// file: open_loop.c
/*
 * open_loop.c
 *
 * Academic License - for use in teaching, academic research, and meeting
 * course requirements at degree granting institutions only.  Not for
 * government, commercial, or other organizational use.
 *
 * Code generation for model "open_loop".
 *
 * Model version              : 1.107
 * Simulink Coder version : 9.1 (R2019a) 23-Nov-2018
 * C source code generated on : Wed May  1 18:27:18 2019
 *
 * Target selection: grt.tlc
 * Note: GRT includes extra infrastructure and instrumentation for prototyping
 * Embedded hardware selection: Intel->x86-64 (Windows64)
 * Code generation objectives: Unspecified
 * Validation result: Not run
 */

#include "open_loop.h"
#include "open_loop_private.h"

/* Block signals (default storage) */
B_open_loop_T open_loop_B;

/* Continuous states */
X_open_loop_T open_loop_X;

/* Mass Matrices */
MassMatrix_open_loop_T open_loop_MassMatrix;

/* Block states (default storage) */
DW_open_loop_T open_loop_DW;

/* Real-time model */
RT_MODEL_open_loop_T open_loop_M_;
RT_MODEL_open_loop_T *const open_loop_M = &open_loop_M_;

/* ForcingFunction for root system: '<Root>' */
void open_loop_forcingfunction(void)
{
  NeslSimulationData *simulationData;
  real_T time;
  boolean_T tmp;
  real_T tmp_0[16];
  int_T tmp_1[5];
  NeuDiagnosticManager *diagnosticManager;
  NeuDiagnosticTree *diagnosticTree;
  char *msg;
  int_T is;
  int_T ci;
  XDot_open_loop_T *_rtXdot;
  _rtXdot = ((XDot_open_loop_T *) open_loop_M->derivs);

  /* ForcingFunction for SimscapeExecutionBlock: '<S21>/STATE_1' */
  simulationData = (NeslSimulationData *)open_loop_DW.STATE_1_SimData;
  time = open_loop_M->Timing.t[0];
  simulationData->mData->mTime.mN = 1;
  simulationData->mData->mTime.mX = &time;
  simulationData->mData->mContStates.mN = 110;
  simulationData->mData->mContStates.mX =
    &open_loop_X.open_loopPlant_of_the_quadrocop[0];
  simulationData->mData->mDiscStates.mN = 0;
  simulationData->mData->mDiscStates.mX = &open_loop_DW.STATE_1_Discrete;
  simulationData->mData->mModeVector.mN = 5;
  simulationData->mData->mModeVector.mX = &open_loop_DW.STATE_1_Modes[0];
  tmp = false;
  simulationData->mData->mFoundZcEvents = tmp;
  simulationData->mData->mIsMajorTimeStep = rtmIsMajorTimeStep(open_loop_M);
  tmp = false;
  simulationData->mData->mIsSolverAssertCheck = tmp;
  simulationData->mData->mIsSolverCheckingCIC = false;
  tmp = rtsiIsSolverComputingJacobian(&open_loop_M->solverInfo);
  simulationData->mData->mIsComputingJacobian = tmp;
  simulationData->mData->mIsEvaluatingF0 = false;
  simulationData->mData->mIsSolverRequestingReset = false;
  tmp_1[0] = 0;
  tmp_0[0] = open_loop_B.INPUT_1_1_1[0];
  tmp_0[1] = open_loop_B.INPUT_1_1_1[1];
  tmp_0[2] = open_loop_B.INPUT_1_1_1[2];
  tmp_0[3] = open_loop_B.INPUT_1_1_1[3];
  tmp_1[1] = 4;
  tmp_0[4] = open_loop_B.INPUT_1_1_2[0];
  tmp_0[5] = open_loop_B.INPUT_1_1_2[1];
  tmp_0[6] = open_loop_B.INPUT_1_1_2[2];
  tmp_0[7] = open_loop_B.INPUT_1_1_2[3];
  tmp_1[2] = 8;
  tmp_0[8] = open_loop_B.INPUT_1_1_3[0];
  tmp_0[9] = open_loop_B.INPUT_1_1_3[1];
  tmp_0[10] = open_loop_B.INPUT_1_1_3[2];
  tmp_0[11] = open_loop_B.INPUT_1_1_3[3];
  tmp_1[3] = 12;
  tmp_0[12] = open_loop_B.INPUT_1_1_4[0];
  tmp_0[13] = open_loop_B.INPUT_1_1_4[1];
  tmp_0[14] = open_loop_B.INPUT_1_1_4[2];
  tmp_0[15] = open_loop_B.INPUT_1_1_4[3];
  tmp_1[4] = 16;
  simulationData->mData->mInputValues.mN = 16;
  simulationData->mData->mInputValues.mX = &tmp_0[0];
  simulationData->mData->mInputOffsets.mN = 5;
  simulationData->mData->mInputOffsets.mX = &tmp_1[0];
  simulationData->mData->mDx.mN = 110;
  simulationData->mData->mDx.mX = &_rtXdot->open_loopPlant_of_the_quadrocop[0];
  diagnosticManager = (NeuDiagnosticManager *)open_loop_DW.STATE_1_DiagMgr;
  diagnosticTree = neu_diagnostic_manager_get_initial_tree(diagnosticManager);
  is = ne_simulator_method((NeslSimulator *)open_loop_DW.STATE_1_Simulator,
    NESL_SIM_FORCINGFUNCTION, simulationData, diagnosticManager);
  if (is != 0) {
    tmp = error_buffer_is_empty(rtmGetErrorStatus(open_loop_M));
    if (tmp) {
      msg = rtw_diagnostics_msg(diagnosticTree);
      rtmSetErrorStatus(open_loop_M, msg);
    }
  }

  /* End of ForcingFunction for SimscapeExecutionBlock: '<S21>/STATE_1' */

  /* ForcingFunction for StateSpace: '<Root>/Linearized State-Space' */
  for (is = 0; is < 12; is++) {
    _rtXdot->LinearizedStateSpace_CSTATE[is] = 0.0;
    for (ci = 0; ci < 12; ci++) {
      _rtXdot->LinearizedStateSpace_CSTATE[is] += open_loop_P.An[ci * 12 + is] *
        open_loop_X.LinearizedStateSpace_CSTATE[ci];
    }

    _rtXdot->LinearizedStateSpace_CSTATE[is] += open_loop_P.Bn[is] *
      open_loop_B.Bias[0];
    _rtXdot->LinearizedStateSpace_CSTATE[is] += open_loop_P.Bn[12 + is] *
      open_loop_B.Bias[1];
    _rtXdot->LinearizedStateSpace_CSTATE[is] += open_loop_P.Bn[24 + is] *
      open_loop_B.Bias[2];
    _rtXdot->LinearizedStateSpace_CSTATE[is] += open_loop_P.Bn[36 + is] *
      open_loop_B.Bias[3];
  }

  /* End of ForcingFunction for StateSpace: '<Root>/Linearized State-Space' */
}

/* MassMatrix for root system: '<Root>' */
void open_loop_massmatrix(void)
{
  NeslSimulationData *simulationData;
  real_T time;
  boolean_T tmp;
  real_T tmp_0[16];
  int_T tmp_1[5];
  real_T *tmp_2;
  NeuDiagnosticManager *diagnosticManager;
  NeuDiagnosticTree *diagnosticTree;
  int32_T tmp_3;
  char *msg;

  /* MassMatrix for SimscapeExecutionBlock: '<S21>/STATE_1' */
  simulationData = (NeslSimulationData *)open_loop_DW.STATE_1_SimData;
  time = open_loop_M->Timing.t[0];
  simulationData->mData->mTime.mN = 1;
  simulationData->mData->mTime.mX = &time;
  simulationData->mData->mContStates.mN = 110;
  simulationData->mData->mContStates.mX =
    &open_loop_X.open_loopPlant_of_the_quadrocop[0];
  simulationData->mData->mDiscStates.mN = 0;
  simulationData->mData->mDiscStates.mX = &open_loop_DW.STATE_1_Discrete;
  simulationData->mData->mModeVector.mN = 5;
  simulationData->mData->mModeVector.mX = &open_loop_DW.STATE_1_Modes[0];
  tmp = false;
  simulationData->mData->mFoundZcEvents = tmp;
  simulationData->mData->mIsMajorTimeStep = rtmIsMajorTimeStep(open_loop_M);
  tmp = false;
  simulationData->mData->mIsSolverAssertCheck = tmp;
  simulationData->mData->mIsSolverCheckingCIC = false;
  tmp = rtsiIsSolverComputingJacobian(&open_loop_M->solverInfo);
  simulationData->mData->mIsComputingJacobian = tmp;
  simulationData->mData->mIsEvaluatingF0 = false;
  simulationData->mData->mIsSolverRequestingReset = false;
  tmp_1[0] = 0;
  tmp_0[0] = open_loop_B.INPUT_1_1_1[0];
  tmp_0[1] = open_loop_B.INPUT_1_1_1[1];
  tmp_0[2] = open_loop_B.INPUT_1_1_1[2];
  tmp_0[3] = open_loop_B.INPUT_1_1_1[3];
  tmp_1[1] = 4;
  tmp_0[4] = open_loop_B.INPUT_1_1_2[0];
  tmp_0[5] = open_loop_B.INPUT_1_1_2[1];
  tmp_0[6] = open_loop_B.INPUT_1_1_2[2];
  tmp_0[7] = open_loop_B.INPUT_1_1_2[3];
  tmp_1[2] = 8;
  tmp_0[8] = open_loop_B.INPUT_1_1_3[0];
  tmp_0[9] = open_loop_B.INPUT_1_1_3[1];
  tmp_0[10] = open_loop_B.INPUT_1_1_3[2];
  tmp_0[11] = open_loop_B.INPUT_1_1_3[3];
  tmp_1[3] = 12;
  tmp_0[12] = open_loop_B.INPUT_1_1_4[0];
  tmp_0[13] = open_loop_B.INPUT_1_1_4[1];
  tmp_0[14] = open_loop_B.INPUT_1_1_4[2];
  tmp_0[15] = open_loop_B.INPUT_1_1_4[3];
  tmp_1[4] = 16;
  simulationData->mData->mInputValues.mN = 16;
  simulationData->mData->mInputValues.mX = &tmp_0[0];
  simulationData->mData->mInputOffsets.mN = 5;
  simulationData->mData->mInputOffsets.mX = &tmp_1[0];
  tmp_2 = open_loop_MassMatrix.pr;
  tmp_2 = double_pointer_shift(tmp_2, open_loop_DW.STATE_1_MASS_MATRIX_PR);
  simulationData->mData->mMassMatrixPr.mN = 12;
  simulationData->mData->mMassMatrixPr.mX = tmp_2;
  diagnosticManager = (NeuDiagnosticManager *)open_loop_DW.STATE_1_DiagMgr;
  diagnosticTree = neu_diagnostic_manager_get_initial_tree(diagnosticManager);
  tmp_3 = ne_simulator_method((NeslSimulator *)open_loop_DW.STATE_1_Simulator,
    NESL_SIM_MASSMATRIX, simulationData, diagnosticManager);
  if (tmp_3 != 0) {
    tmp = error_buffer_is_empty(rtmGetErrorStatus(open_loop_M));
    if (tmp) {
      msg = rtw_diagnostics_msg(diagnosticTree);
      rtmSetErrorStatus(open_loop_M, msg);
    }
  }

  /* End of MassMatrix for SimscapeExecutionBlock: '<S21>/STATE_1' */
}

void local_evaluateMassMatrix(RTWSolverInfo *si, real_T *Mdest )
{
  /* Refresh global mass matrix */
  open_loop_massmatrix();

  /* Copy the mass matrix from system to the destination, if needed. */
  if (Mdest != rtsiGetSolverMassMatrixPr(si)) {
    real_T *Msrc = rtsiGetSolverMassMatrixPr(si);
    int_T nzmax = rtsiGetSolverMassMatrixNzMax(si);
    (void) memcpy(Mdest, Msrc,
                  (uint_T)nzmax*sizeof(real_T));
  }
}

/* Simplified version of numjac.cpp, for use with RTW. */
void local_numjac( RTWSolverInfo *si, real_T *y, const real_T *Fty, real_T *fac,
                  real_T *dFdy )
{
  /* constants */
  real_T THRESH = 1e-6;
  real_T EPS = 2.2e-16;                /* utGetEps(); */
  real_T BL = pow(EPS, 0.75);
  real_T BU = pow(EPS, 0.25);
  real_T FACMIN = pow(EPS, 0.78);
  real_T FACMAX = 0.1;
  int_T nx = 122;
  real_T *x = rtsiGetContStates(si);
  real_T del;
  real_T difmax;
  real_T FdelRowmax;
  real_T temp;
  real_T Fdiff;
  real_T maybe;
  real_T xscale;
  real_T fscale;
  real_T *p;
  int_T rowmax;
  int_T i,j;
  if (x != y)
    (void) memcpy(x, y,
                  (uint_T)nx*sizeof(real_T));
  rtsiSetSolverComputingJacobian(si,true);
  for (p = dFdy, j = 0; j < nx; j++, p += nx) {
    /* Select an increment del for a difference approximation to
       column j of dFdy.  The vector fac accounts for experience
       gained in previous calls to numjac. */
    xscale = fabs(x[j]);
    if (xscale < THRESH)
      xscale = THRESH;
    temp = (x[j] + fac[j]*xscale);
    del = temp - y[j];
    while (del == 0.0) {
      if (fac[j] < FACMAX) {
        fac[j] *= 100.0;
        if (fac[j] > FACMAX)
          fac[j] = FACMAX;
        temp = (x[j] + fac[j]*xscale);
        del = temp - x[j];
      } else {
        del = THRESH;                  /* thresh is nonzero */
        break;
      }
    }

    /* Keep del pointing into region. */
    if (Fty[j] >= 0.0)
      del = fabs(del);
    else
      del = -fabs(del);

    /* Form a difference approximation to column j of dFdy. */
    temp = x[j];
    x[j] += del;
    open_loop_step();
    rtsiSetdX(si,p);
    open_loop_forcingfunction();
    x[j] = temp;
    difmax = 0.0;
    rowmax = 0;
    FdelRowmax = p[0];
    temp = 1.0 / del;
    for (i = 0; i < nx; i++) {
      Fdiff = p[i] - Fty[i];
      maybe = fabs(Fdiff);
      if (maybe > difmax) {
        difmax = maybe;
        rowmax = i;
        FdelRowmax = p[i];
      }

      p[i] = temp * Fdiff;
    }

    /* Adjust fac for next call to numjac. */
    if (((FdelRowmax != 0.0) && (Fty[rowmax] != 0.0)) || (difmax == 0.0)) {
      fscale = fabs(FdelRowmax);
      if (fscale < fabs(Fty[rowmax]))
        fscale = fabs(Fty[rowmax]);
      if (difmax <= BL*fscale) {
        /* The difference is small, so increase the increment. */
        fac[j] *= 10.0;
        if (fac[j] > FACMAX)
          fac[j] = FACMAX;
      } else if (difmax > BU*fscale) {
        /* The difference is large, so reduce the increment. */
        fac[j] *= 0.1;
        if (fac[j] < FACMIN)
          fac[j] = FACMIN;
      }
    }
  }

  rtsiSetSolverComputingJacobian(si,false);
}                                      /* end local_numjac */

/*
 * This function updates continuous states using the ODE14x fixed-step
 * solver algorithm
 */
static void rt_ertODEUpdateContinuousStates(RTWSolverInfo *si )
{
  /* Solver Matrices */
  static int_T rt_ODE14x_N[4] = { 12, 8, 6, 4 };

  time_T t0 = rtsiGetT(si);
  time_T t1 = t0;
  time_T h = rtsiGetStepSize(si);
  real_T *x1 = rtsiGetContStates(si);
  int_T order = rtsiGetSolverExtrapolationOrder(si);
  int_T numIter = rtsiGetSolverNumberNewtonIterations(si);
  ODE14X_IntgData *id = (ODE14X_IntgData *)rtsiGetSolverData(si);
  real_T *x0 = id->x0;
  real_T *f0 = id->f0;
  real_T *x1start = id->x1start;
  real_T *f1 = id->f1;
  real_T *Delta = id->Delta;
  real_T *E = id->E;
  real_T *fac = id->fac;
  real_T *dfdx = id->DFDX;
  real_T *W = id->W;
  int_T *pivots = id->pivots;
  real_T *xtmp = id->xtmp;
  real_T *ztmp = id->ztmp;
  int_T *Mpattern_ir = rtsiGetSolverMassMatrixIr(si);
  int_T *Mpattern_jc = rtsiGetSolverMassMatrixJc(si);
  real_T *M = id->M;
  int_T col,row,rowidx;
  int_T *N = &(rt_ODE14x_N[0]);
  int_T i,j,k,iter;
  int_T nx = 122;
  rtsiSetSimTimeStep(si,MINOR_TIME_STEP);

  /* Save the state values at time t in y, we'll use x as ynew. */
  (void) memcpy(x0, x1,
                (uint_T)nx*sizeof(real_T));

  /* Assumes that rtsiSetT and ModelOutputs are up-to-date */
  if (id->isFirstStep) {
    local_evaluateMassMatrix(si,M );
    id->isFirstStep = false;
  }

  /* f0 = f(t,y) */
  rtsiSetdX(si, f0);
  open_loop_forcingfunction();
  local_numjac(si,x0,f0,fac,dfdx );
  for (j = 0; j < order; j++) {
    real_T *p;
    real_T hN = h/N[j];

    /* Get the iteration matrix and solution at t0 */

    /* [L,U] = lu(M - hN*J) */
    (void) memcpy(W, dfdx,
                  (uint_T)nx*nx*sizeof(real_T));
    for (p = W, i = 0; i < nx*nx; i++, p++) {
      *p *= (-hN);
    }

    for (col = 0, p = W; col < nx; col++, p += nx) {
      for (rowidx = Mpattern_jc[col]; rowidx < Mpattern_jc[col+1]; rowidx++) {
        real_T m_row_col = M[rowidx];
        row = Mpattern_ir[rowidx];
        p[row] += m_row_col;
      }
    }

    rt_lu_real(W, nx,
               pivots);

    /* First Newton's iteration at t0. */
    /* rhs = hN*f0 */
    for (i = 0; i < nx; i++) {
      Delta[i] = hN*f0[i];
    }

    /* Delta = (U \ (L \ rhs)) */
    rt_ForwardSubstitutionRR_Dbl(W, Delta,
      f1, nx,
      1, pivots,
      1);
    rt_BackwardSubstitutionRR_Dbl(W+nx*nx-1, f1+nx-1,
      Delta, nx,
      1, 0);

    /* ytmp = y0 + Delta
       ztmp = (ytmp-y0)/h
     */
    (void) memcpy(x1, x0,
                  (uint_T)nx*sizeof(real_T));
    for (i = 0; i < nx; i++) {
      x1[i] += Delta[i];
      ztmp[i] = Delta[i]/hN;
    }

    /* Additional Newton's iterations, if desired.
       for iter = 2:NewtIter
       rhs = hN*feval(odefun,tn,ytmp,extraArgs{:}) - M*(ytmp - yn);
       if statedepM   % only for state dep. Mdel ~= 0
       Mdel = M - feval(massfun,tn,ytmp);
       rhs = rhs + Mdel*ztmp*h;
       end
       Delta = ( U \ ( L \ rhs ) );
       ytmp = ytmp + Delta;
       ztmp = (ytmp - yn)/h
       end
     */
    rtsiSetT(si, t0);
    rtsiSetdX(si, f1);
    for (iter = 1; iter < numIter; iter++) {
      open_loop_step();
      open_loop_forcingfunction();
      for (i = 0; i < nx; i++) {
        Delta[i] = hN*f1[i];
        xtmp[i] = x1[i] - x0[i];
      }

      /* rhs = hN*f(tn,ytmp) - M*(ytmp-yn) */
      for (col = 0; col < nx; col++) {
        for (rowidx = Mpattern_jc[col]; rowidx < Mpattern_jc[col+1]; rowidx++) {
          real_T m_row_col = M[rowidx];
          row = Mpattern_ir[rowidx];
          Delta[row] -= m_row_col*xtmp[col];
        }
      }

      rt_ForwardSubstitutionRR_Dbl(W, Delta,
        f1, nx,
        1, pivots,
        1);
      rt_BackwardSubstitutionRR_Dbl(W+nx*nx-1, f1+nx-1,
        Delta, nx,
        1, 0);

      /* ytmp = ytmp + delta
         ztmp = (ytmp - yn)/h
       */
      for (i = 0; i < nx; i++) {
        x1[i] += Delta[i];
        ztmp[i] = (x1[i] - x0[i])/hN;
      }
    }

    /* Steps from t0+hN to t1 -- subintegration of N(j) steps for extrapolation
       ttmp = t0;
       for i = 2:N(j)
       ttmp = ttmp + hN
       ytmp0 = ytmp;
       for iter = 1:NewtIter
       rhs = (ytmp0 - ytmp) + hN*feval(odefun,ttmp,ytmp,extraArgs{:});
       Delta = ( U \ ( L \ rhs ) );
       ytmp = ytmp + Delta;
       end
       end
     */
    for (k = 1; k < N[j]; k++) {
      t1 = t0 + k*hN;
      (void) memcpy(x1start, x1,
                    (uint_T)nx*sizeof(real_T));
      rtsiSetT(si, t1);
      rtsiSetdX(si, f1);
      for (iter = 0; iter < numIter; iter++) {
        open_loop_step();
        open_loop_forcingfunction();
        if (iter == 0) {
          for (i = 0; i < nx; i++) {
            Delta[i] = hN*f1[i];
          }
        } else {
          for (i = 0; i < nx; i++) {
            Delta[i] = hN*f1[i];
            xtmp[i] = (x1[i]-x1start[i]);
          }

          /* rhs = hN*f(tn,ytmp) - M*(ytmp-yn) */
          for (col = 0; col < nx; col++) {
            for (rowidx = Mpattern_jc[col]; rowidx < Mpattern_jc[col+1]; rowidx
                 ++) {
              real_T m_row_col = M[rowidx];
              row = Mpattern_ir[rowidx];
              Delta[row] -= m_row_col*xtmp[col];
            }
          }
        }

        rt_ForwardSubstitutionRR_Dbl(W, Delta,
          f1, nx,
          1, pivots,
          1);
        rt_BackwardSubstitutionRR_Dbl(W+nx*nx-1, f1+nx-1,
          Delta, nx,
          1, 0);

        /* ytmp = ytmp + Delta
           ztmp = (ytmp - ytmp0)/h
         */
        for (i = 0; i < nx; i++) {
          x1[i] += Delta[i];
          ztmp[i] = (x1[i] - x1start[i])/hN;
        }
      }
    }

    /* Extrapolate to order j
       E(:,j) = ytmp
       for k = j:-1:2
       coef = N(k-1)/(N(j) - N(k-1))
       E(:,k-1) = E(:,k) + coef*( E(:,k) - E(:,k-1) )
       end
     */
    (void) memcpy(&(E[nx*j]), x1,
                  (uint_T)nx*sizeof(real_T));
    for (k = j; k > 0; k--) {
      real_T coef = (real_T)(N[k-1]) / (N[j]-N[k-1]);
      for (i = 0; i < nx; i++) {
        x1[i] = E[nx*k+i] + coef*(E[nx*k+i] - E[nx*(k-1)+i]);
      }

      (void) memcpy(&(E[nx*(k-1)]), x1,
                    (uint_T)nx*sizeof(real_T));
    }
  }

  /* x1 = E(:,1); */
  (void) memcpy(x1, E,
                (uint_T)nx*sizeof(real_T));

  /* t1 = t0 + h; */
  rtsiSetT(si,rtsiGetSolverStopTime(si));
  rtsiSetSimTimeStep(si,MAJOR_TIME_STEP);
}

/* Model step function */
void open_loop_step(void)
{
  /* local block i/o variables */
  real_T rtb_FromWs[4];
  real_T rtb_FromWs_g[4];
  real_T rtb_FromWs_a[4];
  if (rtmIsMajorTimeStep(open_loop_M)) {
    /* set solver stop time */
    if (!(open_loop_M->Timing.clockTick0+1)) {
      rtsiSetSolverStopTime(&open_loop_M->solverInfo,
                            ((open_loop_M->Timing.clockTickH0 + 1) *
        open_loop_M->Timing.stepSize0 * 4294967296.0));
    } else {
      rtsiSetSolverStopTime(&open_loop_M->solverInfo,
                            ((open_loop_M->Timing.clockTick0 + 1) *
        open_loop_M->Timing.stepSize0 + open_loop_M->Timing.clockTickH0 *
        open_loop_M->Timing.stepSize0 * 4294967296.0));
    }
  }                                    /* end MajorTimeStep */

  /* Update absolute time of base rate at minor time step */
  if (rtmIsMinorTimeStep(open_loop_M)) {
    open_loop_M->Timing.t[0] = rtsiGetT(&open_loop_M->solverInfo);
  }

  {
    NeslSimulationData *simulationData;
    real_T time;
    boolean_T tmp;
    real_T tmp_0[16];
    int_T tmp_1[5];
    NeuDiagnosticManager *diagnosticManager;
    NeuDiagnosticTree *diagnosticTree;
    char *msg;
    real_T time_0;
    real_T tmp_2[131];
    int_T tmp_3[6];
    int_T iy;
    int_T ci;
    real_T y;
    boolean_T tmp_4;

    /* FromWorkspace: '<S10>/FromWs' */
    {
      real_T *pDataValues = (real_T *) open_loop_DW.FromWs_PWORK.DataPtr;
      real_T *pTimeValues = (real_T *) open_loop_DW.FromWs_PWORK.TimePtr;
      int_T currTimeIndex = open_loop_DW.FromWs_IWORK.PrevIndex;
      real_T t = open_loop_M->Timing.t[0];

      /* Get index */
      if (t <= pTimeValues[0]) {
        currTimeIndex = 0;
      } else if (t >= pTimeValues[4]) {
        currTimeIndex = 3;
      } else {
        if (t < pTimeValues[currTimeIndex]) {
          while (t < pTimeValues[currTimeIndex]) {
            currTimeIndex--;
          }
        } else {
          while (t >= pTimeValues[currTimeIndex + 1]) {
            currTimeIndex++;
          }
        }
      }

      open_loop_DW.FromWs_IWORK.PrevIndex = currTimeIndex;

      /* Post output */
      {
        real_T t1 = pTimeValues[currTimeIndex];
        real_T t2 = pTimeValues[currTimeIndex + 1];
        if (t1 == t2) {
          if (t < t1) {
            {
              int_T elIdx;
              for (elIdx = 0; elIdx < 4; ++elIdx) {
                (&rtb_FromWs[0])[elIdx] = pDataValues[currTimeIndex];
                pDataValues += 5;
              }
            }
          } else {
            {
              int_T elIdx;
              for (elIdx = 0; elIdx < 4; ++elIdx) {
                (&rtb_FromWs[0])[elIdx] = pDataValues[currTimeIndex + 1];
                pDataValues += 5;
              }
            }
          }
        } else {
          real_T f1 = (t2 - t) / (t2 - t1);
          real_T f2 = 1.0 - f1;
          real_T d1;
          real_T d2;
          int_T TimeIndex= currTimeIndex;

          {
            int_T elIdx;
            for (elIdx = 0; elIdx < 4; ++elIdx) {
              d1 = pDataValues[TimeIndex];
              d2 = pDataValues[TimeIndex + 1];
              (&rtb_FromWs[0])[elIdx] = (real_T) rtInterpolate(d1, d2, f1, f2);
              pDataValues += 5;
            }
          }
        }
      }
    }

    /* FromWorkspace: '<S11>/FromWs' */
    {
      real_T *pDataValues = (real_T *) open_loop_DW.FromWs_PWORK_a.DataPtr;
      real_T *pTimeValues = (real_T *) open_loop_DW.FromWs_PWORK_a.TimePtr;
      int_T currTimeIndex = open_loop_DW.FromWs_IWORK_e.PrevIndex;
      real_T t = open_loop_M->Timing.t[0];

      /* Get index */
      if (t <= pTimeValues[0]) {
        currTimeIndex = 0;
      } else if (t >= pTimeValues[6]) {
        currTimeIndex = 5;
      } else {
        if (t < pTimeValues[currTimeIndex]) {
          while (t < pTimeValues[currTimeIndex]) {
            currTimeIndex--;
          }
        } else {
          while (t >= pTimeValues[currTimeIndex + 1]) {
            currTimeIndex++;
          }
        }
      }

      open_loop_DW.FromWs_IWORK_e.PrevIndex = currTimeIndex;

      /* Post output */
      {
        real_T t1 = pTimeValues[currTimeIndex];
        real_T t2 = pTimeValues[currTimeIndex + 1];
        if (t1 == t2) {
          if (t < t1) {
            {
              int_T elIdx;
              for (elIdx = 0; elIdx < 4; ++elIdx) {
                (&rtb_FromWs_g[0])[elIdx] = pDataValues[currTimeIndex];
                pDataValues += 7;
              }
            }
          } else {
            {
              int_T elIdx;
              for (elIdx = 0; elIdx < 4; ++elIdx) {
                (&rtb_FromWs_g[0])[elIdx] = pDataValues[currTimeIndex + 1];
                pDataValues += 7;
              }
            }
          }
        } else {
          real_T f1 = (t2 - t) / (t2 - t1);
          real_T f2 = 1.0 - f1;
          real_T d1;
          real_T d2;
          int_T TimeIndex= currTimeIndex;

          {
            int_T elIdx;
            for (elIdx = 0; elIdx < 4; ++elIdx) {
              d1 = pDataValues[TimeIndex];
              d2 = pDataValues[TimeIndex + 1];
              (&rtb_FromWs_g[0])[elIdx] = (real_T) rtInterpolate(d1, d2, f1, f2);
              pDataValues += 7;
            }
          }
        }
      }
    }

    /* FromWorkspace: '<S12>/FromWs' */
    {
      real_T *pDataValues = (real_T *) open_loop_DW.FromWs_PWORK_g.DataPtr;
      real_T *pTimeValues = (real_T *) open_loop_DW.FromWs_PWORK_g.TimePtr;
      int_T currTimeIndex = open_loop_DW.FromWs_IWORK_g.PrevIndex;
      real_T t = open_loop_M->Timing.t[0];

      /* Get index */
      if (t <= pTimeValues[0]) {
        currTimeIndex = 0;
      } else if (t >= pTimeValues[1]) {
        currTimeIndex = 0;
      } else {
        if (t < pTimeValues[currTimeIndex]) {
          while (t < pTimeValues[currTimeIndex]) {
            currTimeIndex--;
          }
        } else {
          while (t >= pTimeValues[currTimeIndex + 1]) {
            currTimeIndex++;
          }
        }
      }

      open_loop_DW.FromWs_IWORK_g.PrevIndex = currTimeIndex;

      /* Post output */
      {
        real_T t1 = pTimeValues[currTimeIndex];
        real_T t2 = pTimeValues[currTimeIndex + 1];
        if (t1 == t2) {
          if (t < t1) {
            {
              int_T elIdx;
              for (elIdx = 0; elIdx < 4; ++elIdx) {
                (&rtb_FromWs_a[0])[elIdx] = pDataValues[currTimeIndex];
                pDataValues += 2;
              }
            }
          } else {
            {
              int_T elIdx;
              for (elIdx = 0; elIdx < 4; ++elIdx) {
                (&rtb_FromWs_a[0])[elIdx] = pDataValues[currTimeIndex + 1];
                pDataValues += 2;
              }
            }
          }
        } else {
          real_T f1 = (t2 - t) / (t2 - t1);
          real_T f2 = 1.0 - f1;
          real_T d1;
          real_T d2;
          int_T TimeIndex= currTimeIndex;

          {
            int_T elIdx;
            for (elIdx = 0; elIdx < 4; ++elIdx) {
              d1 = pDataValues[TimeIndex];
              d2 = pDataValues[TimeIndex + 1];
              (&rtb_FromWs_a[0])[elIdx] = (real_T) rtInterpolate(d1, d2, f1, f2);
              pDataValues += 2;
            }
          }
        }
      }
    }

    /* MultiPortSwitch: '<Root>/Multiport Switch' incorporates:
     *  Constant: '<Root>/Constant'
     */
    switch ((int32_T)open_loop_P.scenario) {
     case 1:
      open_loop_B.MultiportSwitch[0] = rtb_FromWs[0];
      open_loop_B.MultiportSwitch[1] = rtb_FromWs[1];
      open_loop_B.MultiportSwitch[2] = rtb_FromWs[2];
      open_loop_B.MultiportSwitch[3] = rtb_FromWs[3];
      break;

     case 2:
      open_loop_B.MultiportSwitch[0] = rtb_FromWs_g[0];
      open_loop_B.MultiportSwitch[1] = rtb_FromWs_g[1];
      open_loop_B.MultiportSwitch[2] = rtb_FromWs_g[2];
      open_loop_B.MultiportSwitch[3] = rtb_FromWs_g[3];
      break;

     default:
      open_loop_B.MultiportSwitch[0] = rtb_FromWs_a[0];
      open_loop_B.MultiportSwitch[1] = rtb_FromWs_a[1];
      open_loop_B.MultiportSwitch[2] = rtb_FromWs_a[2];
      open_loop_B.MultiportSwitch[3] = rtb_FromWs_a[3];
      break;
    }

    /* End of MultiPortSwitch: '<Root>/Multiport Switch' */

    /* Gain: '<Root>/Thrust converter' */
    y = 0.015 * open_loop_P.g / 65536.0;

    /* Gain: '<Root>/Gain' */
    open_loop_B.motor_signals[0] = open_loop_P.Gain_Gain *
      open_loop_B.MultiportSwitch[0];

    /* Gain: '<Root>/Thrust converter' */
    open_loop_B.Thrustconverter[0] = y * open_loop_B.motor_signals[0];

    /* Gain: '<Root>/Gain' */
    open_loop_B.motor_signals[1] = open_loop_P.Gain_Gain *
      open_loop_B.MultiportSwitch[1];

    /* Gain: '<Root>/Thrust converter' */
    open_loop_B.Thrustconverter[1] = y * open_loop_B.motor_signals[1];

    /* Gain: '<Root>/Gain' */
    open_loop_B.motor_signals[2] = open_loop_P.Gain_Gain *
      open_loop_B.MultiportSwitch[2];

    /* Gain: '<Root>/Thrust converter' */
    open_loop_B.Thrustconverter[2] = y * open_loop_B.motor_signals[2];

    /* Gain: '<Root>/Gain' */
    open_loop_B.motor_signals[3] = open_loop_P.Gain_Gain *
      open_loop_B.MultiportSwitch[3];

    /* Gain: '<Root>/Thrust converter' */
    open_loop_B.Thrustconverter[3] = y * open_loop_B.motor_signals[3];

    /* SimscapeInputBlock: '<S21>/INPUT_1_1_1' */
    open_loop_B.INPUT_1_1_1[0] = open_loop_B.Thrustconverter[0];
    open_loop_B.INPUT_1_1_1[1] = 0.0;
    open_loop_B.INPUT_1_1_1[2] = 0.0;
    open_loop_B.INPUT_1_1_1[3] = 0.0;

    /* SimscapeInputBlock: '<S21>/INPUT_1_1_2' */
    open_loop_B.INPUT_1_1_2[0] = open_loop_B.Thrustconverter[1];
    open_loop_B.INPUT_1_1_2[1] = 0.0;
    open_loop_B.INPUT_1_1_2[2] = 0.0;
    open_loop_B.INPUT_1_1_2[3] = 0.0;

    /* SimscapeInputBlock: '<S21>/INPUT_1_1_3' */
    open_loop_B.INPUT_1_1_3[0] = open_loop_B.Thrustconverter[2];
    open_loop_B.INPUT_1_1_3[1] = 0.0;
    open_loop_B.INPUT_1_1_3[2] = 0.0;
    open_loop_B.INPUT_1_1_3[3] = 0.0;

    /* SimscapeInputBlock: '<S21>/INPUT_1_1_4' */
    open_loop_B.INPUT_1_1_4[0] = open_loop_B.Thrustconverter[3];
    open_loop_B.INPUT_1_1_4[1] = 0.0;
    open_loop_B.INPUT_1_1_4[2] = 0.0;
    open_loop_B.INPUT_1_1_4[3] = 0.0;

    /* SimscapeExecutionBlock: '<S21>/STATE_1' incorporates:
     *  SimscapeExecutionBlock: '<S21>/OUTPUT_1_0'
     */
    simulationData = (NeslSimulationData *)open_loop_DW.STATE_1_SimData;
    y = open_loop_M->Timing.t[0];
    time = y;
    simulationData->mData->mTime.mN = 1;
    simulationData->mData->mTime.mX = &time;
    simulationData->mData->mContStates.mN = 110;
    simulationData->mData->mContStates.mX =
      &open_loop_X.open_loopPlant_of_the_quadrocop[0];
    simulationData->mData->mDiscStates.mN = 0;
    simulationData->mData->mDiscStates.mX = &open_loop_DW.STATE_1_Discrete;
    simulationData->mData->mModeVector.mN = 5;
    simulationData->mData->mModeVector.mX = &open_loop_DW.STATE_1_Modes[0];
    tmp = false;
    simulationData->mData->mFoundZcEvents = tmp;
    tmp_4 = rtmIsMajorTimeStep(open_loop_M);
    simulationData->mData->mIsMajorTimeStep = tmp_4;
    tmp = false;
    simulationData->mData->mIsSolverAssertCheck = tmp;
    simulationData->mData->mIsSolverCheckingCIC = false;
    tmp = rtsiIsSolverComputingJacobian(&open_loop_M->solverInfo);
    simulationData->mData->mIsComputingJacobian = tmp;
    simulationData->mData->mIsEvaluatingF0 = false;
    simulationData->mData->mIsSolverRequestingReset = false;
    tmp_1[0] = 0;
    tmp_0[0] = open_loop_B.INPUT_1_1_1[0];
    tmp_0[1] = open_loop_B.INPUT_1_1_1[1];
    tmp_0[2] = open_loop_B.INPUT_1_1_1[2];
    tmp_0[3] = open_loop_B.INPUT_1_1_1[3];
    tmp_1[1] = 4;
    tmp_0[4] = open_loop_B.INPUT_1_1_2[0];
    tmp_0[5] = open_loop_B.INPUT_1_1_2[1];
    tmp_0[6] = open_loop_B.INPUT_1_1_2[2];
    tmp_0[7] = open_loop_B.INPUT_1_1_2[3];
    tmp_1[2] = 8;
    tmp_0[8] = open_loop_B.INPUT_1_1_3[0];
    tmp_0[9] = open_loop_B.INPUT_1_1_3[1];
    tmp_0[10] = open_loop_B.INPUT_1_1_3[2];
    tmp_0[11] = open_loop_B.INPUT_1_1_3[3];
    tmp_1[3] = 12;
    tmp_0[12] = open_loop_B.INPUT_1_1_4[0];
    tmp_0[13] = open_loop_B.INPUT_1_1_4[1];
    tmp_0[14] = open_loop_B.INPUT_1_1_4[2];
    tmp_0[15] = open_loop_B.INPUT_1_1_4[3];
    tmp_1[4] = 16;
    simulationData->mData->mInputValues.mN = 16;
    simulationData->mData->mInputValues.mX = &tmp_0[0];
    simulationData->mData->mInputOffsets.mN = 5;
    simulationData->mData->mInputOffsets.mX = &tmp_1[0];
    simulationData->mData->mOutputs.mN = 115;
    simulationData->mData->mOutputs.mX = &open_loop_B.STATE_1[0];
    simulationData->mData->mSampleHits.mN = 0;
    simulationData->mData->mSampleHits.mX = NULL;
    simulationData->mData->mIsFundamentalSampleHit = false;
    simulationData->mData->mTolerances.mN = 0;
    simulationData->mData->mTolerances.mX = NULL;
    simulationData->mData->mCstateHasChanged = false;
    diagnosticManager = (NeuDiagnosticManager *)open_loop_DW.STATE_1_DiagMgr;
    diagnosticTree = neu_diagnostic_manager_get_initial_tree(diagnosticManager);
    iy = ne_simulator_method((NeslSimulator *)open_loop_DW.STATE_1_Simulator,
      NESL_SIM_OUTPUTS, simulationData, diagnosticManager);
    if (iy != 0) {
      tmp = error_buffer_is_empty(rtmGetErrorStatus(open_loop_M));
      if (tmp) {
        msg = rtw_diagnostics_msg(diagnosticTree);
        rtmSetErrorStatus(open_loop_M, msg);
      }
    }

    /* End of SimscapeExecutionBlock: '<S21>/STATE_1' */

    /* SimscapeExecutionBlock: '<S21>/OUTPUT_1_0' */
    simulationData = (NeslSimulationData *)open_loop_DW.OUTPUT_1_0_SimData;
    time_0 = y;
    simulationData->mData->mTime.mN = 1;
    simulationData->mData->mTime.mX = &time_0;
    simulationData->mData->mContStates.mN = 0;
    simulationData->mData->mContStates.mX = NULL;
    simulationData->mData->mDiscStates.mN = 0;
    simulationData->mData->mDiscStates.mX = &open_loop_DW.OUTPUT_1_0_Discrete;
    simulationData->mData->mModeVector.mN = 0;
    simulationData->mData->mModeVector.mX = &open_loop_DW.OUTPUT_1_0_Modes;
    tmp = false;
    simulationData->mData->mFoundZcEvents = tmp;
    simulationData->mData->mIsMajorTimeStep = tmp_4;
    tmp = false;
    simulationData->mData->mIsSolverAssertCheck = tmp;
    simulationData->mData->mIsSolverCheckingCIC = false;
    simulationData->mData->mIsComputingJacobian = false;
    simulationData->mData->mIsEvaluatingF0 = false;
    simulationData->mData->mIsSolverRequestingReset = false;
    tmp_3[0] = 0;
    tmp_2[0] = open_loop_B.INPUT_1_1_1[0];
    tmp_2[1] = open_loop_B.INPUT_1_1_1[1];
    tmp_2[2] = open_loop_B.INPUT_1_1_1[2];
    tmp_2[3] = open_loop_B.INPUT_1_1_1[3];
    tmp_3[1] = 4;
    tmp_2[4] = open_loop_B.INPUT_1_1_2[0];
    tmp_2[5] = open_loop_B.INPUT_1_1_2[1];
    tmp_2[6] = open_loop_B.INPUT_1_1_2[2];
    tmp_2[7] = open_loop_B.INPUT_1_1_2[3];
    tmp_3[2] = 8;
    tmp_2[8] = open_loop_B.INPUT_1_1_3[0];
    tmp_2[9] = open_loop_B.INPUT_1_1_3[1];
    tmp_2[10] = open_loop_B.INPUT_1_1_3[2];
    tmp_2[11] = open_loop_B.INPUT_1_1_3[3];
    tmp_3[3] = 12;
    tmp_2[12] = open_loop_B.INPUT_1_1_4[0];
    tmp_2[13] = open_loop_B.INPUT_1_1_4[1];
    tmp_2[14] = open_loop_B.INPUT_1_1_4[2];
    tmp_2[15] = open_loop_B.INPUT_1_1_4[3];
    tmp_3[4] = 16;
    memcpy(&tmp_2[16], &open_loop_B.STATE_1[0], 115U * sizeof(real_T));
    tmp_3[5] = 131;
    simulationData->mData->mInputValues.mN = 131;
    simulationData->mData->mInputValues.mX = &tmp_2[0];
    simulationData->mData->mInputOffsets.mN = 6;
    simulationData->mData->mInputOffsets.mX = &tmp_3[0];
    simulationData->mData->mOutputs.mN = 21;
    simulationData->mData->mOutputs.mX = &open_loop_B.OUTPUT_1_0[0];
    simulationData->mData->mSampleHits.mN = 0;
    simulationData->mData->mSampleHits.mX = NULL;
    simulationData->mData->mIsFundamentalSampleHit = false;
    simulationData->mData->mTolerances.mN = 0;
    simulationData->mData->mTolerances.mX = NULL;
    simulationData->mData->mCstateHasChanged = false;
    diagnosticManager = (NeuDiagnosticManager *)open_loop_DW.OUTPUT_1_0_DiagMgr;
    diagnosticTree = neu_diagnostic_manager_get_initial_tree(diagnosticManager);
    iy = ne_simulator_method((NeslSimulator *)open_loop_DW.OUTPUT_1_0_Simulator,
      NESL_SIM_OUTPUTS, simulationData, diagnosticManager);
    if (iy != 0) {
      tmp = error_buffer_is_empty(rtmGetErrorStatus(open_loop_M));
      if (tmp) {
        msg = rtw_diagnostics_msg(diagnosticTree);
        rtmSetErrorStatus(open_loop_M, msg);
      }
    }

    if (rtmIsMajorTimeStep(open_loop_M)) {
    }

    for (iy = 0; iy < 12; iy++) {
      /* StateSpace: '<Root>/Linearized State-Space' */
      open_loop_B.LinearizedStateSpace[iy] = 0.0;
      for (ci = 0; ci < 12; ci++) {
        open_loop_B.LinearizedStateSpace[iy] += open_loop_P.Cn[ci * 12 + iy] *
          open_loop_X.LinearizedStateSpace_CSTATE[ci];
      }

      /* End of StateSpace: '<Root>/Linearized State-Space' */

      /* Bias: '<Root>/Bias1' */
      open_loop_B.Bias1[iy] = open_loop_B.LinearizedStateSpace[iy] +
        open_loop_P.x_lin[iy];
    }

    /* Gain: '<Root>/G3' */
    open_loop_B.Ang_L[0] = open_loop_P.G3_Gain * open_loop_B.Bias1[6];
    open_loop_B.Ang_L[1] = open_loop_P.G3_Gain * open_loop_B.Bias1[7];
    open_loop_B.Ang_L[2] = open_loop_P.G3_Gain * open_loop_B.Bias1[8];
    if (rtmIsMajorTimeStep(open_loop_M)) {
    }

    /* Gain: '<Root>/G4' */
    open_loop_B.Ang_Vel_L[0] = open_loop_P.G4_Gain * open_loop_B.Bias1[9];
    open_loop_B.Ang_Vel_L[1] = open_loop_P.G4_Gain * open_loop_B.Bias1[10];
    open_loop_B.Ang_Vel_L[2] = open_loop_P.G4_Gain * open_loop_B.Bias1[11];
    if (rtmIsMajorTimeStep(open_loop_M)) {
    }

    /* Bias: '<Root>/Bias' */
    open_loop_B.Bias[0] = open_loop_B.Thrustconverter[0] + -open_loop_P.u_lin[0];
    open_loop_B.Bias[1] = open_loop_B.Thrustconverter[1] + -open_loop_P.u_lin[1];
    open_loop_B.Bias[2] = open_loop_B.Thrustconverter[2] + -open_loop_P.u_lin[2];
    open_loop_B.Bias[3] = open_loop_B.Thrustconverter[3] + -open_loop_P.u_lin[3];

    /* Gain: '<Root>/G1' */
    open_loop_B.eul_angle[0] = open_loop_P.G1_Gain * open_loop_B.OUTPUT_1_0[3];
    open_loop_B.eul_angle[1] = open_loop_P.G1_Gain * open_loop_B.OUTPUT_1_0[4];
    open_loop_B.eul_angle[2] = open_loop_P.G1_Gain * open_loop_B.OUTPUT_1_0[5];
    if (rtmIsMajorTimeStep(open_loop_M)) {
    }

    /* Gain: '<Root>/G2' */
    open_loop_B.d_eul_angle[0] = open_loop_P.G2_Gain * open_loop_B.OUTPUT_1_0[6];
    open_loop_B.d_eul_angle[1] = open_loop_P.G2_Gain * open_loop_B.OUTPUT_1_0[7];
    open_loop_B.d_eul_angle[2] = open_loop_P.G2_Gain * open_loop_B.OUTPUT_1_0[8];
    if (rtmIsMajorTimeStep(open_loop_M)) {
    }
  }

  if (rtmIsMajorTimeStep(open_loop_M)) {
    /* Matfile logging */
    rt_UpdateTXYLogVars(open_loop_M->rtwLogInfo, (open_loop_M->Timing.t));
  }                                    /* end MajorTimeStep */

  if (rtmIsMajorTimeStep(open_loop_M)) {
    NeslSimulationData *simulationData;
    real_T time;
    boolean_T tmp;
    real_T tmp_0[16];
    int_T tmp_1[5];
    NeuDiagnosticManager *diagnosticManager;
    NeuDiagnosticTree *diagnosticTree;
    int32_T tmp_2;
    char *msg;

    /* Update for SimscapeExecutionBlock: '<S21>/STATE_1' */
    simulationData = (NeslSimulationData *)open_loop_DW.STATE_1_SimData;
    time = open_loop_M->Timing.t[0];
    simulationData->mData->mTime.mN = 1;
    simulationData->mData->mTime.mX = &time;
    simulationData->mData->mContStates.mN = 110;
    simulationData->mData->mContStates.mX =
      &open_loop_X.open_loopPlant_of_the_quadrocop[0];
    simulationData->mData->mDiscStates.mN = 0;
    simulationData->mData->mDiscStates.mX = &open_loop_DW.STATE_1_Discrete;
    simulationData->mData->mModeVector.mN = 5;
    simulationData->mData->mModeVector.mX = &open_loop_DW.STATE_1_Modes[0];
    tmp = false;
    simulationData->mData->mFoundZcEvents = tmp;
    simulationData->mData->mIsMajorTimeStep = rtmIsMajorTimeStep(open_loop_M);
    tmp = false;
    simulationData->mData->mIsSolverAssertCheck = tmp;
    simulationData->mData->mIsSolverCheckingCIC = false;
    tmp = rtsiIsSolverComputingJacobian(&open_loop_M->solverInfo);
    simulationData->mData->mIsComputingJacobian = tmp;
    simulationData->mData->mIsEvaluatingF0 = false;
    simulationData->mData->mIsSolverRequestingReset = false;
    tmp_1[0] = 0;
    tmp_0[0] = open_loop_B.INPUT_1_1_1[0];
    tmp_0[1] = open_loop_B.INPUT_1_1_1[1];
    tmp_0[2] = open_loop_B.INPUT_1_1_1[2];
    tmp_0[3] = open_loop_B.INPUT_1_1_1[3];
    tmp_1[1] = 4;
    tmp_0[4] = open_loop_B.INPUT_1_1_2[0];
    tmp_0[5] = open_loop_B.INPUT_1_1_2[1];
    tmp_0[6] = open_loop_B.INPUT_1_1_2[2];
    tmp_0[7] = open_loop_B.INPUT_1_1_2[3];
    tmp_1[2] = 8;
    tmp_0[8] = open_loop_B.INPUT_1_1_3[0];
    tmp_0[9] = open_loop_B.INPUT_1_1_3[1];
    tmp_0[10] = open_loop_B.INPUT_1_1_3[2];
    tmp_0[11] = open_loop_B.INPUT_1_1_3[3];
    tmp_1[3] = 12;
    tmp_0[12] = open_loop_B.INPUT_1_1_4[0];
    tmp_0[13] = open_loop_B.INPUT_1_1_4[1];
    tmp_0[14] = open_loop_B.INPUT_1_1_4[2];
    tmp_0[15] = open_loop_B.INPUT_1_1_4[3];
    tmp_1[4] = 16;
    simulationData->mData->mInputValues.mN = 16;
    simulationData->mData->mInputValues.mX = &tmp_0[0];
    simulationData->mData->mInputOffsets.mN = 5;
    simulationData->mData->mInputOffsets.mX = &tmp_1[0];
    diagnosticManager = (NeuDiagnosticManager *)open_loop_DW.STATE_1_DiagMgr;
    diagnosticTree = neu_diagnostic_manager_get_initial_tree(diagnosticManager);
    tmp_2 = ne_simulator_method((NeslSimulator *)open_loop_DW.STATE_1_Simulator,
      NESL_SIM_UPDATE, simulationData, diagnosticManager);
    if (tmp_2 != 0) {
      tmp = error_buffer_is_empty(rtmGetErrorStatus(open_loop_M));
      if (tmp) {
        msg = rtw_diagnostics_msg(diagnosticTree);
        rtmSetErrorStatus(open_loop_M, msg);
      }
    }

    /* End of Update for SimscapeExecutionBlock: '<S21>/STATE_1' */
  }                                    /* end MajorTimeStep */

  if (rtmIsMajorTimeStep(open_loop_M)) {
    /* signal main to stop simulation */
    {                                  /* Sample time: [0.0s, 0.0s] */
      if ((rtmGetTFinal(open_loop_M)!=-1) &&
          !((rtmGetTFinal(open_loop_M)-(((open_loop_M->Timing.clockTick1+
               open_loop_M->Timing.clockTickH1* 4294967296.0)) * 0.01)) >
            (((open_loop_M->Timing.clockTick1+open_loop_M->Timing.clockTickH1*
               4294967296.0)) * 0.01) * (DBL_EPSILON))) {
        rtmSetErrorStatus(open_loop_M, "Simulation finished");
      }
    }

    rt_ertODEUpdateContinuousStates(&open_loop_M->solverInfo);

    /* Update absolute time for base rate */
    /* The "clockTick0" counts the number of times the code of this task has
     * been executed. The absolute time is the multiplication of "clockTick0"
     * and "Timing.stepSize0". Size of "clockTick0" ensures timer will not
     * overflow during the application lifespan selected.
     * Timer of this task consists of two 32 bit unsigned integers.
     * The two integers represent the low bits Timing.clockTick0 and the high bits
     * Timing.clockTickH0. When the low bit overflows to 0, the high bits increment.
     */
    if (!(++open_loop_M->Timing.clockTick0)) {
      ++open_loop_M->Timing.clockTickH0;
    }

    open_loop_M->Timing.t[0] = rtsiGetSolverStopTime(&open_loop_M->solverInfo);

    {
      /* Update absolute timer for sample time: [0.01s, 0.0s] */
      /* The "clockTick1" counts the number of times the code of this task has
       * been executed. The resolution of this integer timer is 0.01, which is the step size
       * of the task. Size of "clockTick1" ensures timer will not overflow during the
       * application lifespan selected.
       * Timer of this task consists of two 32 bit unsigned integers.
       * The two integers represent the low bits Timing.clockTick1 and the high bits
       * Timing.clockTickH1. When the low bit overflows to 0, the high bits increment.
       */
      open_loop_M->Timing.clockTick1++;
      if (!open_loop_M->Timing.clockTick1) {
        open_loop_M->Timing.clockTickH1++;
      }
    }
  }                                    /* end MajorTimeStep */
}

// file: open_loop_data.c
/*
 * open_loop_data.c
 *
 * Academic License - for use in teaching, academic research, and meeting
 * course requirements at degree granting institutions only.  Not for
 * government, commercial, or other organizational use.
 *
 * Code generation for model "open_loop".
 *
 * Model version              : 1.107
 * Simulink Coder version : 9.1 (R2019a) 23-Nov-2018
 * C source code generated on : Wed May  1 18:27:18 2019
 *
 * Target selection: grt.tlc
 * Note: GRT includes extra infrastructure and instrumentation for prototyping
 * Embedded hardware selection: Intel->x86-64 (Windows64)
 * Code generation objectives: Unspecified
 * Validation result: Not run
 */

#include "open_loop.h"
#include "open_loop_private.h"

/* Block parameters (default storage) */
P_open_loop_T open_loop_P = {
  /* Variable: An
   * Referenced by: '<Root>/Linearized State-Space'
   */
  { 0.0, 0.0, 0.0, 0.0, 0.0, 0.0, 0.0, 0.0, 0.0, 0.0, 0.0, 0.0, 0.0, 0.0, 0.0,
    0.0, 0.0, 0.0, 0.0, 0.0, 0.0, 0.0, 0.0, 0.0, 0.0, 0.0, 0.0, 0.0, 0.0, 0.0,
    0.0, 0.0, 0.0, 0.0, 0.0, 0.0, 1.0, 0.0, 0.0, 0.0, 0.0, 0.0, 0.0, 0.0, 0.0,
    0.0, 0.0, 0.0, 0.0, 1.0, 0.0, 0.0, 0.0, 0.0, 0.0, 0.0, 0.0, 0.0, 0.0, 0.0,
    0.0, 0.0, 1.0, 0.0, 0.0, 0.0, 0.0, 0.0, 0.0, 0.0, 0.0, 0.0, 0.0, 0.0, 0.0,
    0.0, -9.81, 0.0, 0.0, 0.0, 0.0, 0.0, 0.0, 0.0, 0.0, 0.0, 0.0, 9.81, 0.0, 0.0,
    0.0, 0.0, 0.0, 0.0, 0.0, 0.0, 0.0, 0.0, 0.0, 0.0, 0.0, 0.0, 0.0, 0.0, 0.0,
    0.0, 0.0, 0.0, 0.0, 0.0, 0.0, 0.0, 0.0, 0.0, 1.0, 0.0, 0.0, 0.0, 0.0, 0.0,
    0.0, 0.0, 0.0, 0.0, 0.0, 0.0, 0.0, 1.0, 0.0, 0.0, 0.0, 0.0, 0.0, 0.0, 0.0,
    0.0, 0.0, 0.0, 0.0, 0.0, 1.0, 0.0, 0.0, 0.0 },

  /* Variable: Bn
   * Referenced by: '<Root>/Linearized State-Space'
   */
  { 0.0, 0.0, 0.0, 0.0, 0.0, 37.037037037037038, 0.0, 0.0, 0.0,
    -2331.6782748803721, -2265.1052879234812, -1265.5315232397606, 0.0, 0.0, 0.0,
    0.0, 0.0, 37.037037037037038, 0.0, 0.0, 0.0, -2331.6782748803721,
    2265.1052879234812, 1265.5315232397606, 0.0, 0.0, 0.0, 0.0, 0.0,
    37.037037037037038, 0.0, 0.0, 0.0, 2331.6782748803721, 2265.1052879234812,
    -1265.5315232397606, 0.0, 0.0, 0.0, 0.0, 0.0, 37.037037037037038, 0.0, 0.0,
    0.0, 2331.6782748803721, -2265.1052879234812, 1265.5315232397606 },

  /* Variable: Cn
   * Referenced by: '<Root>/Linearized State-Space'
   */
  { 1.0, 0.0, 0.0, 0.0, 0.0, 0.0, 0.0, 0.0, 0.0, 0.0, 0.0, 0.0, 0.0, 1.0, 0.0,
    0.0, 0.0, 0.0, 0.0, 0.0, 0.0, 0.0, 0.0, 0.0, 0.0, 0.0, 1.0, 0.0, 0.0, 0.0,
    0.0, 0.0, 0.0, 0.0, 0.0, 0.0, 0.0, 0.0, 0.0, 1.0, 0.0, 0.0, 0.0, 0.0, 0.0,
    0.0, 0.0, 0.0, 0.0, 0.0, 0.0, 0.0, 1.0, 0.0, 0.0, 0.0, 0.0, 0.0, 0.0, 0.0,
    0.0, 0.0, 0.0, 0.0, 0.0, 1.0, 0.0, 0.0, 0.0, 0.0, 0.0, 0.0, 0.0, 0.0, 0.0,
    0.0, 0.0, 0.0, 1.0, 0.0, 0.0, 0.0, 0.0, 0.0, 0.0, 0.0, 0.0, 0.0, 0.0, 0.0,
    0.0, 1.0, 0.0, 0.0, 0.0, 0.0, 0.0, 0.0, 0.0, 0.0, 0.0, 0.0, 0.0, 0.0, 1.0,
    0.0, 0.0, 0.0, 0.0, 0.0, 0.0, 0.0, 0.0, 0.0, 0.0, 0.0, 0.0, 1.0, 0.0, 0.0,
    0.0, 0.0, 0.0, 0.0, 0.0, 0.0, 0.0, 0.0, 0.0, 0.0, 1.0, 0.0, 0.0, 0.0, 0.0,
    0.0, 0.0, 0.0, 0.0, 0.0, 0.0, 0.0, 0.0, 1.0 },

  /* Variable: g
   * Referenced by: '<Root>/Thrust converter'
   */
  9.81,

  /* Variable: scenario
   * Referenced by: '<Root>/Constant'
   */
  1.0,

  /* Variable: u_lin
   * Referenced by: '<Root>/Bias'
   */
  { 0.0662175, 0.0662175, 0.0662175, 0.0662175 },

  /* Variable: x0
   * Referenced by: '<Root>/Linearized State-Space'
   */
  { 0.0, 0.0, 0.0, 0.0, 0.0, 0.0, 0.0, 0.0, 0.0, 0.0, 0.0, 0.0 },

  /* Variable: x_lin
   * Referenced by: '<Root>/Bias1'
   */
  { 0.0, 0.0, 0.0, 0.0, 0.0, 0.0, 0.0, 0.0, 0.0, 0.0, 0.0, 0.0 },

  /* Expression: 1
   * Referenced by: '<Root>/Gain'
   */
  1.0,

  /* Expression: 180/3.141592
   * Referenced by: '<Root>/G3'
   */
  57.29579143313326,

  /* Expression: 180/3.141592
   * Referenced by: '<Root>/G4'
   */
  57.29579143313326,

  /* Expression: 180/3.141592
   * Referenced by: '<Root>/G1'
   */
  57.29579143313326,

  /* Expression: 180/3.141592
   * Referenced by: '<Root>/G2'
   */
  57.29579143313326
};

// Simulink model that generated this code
simulink model "open_loop"  (R2019a)
settings: Solver=FixedStepAuto  StartTime=0.0  StopTime=10.0  FixedStep=1/100  RelTol=1e-3  AbsTol=1e-3
model workspace: external: MATLAB File params.m (data not in the file)
values from neighbouring files (symbols this model uses):
  An = double(subs(A, [x;ctrl] , [x_lin; u_lin] ))    [linearization.m]
  b = 2.75E-11    (= 2.75e-11)    [linearization.m]    (also in main.m)
  Bn = double(subs(B, [x;ctrl] , [x_lin; u_lin] ))    [linearization.m]
  Cn = eye(size(x,1))    [linearization.m]
  Dn = zeros(size(x,1),4)    [linearization.m]
  g = 9.81    [linearization.m]    (also in main.m)
  k = 1E-9    (= 1e-09)    [linearization.m]    (also in main.m)
  m = 0.027    [linearization.m]    (also in main.m)
  scenario = 1    [main.m]
  u_lin = repmat(0.027*g/4, [4 1])    [main.m]
  x0 = [0 0 0  0 0 0  deg2rad(20) deg2rad(20) deg2rad(0) 0 0 0]'    [main.m]
  x_lin = zeros(12,1)    [main.m]
undefined symbols (not defined in the file or in its folder): sigbuilder_block
libraries: nesl_utility x9

== system open_loop ==
  note: Input generator
      | (type should be uint16)
  note: Plant model
  Acc. data : Scope
  Acceleration : Scope
  Ang_L : Scope
  Ang_vel_L : Scope
  Angle : Scope
  Angular velocity : Scope
  Bias : Bias  Bias=-u_lin
  Bias1 : Bias  Bias=+x_lin
  Constant : Constant  Value=scenario
  Demux : Demux
  G{1..4} (4 alike) : Gain  Gain=180/3.141592
  Gain : Gain
  Gyro. data : Scope
  Linearized State-Space : StateSpace  A=An  B=Bn  C=Cn  D=Dn  InitialCondition=x0
  MotorSignals : Scope
  Multiport Switch : MultiPortSwitch
  Mux1 : Mux
  Mux2 : Mux
  Mux3 : Mux
  PS -> S {1..7} (7 alike) : nesl_utility/PS-Simulink Converter  PhysicalDomain=network_engine_domain  SubClassName=ps_output  LeftPortType=input  RightPortType=output  PseudoPeriodic=off  Frequencies=[]  Unit=1  AffineConversion=off
  Plant of the quadrocopter : SimscapeComponentBlock  SourceFile=plant  ComponentPath=plant  ComponentVariants=plant  ComponentVariantNames=plant  ClassName=plant  SchemaVersion=1  m=m kg  g=g m/s^2  d=d m  k=k s^2*N/rad^2  b=b N*m/(rad/s)^2
  Plant of the quadrocopter1 : SimscapeComponentBlock  SourceFile=sensors  ComponentPath=sensors  ComponentVariants=sensors  ComponentVariantNames=sensors  ClassName=sensors  SchemaVersion=1  m=m kg  g=g m/s^2  d=d m  k=k  b=b
  Pos_L : Scope
  Position : Scope
  Simulink-PS Converter : nesl_utility/Simulink-PS Converter  PhysicalDomain=network_engine_domain  SubClassName=ps_input  LeftPortType=input  RightPortType=output  PseudoPeriodic=off  Frequencies=[]  NoiseDistribution=none  NoiseParameters=[]  Unit=1  AffineConversion=off  FilteringAndDerivatives=zero  SimscapeFilterOrder=1  InputFilterTimeConstant=0.001  UdotUserProvided=1
  Solver Configuration : nesl_utility/Solver Configuration  PhysicalDomain=network_engine_domain  SubClassName=solver  LeftPortType=input  RightPortType=generic  Tones=[]  Harmonics=[]  SimulateNoise=off  Profile=off  UseLocalSampling=off  EnableSwitchedLinearOptims=on  FrequencyDomain=off  UseCCode=off  RelTol=0.001  AbsTol=1e-06  MinStep=1e-09  ToWorkspace=off  RevertToSquareIcSolve=off  NumHomotopyIterations=100  PhasorMode=off  PhasorModeNumHarmonics=1  DoDC=off  ResidualTolerance=1e-09  UseLocalSolver=off  LocalSolverChoice=NE_BACKWARD_EULER_ADVANCER  LocalSolverSampleTime=0.001  DoFixedCost=off  MaxNonlinIter=3  MaxModeIter=2  LinearAlgebra=Sparse  EquationFormulation=NE_TIME_EF  DelaysMemoryBudget=1024  AutomaticFiltering=on  FilteringTimeConstant=0.001  PartitionStorageMethod=AS_NEEDED  PartitionMemoryBudget=1024  PartitionMethod=FAST
  Thrust : Scope
  Thrust converter : Gain  Gain=0.06/4*g/65536
  ToDouble : DataTypeConversion  OutDataTypeStr=double  RndMeth=Round  SaturateOnIntegerOverflow=on
  Vel_L : Scope
  Velocity : Scope
  scenario 1 : Subsystem  Tag=STV Subsys  LoadFcn=sigbuilder_block('load');  StartFcn=sigbuilder_block('start');  StopFcn=sigbuilder_block('stop');  ClipboardFcn=sigbuilder_block('clipboard');  mask(Sigbuilder block){tuvar=[0:10]}
      mask help: Simulink:masks:SigbuilderBlock_MD
      mask init:
      | if ~strcmp(get_param(bdroot(gcbh),'SimulationStatus'),'stopped') tuvar = sigbuilder_block('maskInit'); end
  scenario 2 : Subsystem  Tag=STV Subsys  LoadFcn=sigbuilder_block('load');  StartFcn=sigbuilder_block('start');  StopFcn=sigbuilder_block('stop');  ClipboardFcn=sigbuilder_block('clipboard');  mask(Sigbuilder block){tuvar=[0:10]}
      mask help: Simulink:masks:SigbuilderBlock_MD
      mask init:
      | if ~strcmp(get_param(bdroot(gcbh),'SimulationStatus'),'stopped') tuvar = sigbuilder_block('maskInit'); end
  scenario 3 : Subsystem  Tag=STV Subsys  LoadFcn=sigbuilder_block('load');  StartFcn=sigbuilder_block('start');  StopFcn=sigbuilder_block('stop');  ClipboardFcn=sigbuilder_block('clipboard');  mask(Sigbuilder block){tuvar=[0:10]}
      mask help: Simulink:masks:SigbuilderBlock_MD
      mask init:
      | if ~strcmp(get_param(bdroot(gcbh),'SimulationStatus'),'stopped') tuvar = sigbuilder_block('maskInit'); end
  wires:
  "PS -> S 7"/1 -> Gyro. data/1  "gyro_data"
  "PS -> S 6"/1 -> Acc. data/1  "acc_data"
  Multiport Switch/1 -> Gain/1
  G1/1 -> Angle/1  "eul_angle"
  G2/1 -> Angular velocity/1  "d_eul_angle"
  ToDouble/1 -> Thrust converter/1
  Thrust converter/1 -> Bias/1, Simulink-PS Converter/1, Thrust/1
  "PS -> S 1"/1 -> Position/1  "pos"
  "PS -> S 5"/1 -> G2/1
  "PS -> S 4"/1 -> G1/1
  "PS -> S 3"/1 -> Acceleration/1  "acc"
  "PS -> S 2"/1 -> Velocity/1  "vel"
  scenario 1/2(Signal 2) -> Mux3/2
  scenario 1/1(Signal 1) -> Mux3/1
  scenario 1/3(Signal 3) -> Mux3/3
  scenario 1/4(Signal 4) -> Mux3/4
  scenario 2/3(Signal 3) -> Mux1/3
  scenario 2/4(Signal 4) -> Mux1/4
  scenario 2/2(Signal 2) -> Mux1/2
  Mux1/1 -> Multiport Switch/3
  scenario 2/1(Signal 1) -> Mux1/1
  Mux3/1 -> Multiport Switch/2
  Gain/1 -> MotorSignals/1, ToDouble/1  "motor_signals"
  scenario 3/3(Signal 3) -> Mux2/3
  scenario 3/4(Signal 4) -> Mux2/4
  scenario 3/2(Signal 2) -> Mux2/2
  scenario 3/1(Signal 1) -> Mux2/1
  Mux2/1 -> Multiport Switch/4
  Constant/1 -> Multiport Switch/1
  Linearized State-Space/1 -> Bias1/1
  Demux/1 -> Pos_L/1  "Pos_L"
  Demux/2 -> Vel_L/1  "Vel_L"
  Bias/1 -> Linearized State-Space/1
  Bias1/1 -> Demux/1
  G3/1 -> Ang_L/1  "Ang_L"
  Demux/3 -> G3/1  "Ang_L"
  G4/1 -> Ang_vel_L/1  "Ang_Vel_L"
  Demux/4 -> G4/1  "Ang_Vel_L"
  connections:
  Plant of the quadrocopter/LConn1 -- Solver Configuration/RConn1 -- Simulink-PS Converter/RConn1
  Plant of the quadrocopter/RConn1 -- "PS -> S 1"/LConn1 -- Plant of the quadrocopter1/LConn1
  Plant of the quadrocopter/RConn2 -- "PS -> S 2"/LConn1 -- Plant of the quadrocopter1/LConn2
  Plant of the quadrocopter/RConn3 -- "PS -> S 3"/LConn1 -- Plant of the quadrocopter1/LConn3
  Plant of the quadrocopter/RConn4 -- "PS -> S 4"/LConn1 -- Plant of the quadrocopter1/LConn4
  Plant of the quadrocopter/RConn5 -- "PS -> S 5"/LConn1 -- Plant of the quadrocopter1/LConn5
  Plant of the quadrocopter1/RConn1 -- "PS -> S 6"/LConn1
  Plant of the quadrocopter1/RConn2 -- "PS -> S 7"/LConn1

== system open_loop/scenario 1 ==
  Demux : Demux  Tag=STV Demux
  FromWs : FromWorkspace  Tag=STV FromWs  VariableName=tuvar  SampleTime=0
  Signal 1 : Outport  Tag=STV Outport
  Signal 2 : Outport  Tag=STV Outport  Port=2
  Signal 3 : Outport  Tag=STV Outport  Port=3
  Signal 4 : Outport  Tag=STV Outport  Port=4
  wires:
  FromWs/1 -> Demux/1
  Demux/1 -> Signal 1/1
  Demux/2 -> Signal 2/1
  Demux/3 -> Signal 3/1
  Demux/4 -> Signal 4/1

== system open_loop/scenario 2 ==
  Demux : Demux  Tag=STV Demux
  FromWs : FromWorkspace  Tag=STV FromWs  VariableName=tuvar  SampleTime=0
  Signal 1 : Outport  Tag=STV Outport
  Signal 2 : Outport  Tag=STV Outport  Port=2
  Signal 3 : Outport  Tag=STV Outport  Port=3
  Signal 4 : Outport  Tag=STV Outport  Port=4
  wires:
  FromWs/1 -> Demux/1
  Demux/1 -> Signal 1/1
  Demux/2 -> Signal 2/1
  Demux/3 -> Signal 3/1
  Demux/4 -> Signal 4/1

== system open_loop/scenario 3 ==
  Demux : Demux  Tag=STV Demux
  FromWs : FromWorkspace  Tag=STV FromWs  VariableName=tuvar  SampleTime=0
  Signal 1 : Outport  Tag=STV Outport
  Signal 2 : Outport  Tag=STV Outport  Port=2
  Signal 3 : Outport  Tag=STV Outport  Port=3
  Signal 4 : Outport  Tag=STV Outport  Port=4
  wires:
  FromWs/1 -> Demux/1
  Demux/1 -> Signal 1/1
  Demux/2 -> Signal 2/1
  Demux/3 -> Signal 3/1
  Demux/4 -> Signal 4/1
